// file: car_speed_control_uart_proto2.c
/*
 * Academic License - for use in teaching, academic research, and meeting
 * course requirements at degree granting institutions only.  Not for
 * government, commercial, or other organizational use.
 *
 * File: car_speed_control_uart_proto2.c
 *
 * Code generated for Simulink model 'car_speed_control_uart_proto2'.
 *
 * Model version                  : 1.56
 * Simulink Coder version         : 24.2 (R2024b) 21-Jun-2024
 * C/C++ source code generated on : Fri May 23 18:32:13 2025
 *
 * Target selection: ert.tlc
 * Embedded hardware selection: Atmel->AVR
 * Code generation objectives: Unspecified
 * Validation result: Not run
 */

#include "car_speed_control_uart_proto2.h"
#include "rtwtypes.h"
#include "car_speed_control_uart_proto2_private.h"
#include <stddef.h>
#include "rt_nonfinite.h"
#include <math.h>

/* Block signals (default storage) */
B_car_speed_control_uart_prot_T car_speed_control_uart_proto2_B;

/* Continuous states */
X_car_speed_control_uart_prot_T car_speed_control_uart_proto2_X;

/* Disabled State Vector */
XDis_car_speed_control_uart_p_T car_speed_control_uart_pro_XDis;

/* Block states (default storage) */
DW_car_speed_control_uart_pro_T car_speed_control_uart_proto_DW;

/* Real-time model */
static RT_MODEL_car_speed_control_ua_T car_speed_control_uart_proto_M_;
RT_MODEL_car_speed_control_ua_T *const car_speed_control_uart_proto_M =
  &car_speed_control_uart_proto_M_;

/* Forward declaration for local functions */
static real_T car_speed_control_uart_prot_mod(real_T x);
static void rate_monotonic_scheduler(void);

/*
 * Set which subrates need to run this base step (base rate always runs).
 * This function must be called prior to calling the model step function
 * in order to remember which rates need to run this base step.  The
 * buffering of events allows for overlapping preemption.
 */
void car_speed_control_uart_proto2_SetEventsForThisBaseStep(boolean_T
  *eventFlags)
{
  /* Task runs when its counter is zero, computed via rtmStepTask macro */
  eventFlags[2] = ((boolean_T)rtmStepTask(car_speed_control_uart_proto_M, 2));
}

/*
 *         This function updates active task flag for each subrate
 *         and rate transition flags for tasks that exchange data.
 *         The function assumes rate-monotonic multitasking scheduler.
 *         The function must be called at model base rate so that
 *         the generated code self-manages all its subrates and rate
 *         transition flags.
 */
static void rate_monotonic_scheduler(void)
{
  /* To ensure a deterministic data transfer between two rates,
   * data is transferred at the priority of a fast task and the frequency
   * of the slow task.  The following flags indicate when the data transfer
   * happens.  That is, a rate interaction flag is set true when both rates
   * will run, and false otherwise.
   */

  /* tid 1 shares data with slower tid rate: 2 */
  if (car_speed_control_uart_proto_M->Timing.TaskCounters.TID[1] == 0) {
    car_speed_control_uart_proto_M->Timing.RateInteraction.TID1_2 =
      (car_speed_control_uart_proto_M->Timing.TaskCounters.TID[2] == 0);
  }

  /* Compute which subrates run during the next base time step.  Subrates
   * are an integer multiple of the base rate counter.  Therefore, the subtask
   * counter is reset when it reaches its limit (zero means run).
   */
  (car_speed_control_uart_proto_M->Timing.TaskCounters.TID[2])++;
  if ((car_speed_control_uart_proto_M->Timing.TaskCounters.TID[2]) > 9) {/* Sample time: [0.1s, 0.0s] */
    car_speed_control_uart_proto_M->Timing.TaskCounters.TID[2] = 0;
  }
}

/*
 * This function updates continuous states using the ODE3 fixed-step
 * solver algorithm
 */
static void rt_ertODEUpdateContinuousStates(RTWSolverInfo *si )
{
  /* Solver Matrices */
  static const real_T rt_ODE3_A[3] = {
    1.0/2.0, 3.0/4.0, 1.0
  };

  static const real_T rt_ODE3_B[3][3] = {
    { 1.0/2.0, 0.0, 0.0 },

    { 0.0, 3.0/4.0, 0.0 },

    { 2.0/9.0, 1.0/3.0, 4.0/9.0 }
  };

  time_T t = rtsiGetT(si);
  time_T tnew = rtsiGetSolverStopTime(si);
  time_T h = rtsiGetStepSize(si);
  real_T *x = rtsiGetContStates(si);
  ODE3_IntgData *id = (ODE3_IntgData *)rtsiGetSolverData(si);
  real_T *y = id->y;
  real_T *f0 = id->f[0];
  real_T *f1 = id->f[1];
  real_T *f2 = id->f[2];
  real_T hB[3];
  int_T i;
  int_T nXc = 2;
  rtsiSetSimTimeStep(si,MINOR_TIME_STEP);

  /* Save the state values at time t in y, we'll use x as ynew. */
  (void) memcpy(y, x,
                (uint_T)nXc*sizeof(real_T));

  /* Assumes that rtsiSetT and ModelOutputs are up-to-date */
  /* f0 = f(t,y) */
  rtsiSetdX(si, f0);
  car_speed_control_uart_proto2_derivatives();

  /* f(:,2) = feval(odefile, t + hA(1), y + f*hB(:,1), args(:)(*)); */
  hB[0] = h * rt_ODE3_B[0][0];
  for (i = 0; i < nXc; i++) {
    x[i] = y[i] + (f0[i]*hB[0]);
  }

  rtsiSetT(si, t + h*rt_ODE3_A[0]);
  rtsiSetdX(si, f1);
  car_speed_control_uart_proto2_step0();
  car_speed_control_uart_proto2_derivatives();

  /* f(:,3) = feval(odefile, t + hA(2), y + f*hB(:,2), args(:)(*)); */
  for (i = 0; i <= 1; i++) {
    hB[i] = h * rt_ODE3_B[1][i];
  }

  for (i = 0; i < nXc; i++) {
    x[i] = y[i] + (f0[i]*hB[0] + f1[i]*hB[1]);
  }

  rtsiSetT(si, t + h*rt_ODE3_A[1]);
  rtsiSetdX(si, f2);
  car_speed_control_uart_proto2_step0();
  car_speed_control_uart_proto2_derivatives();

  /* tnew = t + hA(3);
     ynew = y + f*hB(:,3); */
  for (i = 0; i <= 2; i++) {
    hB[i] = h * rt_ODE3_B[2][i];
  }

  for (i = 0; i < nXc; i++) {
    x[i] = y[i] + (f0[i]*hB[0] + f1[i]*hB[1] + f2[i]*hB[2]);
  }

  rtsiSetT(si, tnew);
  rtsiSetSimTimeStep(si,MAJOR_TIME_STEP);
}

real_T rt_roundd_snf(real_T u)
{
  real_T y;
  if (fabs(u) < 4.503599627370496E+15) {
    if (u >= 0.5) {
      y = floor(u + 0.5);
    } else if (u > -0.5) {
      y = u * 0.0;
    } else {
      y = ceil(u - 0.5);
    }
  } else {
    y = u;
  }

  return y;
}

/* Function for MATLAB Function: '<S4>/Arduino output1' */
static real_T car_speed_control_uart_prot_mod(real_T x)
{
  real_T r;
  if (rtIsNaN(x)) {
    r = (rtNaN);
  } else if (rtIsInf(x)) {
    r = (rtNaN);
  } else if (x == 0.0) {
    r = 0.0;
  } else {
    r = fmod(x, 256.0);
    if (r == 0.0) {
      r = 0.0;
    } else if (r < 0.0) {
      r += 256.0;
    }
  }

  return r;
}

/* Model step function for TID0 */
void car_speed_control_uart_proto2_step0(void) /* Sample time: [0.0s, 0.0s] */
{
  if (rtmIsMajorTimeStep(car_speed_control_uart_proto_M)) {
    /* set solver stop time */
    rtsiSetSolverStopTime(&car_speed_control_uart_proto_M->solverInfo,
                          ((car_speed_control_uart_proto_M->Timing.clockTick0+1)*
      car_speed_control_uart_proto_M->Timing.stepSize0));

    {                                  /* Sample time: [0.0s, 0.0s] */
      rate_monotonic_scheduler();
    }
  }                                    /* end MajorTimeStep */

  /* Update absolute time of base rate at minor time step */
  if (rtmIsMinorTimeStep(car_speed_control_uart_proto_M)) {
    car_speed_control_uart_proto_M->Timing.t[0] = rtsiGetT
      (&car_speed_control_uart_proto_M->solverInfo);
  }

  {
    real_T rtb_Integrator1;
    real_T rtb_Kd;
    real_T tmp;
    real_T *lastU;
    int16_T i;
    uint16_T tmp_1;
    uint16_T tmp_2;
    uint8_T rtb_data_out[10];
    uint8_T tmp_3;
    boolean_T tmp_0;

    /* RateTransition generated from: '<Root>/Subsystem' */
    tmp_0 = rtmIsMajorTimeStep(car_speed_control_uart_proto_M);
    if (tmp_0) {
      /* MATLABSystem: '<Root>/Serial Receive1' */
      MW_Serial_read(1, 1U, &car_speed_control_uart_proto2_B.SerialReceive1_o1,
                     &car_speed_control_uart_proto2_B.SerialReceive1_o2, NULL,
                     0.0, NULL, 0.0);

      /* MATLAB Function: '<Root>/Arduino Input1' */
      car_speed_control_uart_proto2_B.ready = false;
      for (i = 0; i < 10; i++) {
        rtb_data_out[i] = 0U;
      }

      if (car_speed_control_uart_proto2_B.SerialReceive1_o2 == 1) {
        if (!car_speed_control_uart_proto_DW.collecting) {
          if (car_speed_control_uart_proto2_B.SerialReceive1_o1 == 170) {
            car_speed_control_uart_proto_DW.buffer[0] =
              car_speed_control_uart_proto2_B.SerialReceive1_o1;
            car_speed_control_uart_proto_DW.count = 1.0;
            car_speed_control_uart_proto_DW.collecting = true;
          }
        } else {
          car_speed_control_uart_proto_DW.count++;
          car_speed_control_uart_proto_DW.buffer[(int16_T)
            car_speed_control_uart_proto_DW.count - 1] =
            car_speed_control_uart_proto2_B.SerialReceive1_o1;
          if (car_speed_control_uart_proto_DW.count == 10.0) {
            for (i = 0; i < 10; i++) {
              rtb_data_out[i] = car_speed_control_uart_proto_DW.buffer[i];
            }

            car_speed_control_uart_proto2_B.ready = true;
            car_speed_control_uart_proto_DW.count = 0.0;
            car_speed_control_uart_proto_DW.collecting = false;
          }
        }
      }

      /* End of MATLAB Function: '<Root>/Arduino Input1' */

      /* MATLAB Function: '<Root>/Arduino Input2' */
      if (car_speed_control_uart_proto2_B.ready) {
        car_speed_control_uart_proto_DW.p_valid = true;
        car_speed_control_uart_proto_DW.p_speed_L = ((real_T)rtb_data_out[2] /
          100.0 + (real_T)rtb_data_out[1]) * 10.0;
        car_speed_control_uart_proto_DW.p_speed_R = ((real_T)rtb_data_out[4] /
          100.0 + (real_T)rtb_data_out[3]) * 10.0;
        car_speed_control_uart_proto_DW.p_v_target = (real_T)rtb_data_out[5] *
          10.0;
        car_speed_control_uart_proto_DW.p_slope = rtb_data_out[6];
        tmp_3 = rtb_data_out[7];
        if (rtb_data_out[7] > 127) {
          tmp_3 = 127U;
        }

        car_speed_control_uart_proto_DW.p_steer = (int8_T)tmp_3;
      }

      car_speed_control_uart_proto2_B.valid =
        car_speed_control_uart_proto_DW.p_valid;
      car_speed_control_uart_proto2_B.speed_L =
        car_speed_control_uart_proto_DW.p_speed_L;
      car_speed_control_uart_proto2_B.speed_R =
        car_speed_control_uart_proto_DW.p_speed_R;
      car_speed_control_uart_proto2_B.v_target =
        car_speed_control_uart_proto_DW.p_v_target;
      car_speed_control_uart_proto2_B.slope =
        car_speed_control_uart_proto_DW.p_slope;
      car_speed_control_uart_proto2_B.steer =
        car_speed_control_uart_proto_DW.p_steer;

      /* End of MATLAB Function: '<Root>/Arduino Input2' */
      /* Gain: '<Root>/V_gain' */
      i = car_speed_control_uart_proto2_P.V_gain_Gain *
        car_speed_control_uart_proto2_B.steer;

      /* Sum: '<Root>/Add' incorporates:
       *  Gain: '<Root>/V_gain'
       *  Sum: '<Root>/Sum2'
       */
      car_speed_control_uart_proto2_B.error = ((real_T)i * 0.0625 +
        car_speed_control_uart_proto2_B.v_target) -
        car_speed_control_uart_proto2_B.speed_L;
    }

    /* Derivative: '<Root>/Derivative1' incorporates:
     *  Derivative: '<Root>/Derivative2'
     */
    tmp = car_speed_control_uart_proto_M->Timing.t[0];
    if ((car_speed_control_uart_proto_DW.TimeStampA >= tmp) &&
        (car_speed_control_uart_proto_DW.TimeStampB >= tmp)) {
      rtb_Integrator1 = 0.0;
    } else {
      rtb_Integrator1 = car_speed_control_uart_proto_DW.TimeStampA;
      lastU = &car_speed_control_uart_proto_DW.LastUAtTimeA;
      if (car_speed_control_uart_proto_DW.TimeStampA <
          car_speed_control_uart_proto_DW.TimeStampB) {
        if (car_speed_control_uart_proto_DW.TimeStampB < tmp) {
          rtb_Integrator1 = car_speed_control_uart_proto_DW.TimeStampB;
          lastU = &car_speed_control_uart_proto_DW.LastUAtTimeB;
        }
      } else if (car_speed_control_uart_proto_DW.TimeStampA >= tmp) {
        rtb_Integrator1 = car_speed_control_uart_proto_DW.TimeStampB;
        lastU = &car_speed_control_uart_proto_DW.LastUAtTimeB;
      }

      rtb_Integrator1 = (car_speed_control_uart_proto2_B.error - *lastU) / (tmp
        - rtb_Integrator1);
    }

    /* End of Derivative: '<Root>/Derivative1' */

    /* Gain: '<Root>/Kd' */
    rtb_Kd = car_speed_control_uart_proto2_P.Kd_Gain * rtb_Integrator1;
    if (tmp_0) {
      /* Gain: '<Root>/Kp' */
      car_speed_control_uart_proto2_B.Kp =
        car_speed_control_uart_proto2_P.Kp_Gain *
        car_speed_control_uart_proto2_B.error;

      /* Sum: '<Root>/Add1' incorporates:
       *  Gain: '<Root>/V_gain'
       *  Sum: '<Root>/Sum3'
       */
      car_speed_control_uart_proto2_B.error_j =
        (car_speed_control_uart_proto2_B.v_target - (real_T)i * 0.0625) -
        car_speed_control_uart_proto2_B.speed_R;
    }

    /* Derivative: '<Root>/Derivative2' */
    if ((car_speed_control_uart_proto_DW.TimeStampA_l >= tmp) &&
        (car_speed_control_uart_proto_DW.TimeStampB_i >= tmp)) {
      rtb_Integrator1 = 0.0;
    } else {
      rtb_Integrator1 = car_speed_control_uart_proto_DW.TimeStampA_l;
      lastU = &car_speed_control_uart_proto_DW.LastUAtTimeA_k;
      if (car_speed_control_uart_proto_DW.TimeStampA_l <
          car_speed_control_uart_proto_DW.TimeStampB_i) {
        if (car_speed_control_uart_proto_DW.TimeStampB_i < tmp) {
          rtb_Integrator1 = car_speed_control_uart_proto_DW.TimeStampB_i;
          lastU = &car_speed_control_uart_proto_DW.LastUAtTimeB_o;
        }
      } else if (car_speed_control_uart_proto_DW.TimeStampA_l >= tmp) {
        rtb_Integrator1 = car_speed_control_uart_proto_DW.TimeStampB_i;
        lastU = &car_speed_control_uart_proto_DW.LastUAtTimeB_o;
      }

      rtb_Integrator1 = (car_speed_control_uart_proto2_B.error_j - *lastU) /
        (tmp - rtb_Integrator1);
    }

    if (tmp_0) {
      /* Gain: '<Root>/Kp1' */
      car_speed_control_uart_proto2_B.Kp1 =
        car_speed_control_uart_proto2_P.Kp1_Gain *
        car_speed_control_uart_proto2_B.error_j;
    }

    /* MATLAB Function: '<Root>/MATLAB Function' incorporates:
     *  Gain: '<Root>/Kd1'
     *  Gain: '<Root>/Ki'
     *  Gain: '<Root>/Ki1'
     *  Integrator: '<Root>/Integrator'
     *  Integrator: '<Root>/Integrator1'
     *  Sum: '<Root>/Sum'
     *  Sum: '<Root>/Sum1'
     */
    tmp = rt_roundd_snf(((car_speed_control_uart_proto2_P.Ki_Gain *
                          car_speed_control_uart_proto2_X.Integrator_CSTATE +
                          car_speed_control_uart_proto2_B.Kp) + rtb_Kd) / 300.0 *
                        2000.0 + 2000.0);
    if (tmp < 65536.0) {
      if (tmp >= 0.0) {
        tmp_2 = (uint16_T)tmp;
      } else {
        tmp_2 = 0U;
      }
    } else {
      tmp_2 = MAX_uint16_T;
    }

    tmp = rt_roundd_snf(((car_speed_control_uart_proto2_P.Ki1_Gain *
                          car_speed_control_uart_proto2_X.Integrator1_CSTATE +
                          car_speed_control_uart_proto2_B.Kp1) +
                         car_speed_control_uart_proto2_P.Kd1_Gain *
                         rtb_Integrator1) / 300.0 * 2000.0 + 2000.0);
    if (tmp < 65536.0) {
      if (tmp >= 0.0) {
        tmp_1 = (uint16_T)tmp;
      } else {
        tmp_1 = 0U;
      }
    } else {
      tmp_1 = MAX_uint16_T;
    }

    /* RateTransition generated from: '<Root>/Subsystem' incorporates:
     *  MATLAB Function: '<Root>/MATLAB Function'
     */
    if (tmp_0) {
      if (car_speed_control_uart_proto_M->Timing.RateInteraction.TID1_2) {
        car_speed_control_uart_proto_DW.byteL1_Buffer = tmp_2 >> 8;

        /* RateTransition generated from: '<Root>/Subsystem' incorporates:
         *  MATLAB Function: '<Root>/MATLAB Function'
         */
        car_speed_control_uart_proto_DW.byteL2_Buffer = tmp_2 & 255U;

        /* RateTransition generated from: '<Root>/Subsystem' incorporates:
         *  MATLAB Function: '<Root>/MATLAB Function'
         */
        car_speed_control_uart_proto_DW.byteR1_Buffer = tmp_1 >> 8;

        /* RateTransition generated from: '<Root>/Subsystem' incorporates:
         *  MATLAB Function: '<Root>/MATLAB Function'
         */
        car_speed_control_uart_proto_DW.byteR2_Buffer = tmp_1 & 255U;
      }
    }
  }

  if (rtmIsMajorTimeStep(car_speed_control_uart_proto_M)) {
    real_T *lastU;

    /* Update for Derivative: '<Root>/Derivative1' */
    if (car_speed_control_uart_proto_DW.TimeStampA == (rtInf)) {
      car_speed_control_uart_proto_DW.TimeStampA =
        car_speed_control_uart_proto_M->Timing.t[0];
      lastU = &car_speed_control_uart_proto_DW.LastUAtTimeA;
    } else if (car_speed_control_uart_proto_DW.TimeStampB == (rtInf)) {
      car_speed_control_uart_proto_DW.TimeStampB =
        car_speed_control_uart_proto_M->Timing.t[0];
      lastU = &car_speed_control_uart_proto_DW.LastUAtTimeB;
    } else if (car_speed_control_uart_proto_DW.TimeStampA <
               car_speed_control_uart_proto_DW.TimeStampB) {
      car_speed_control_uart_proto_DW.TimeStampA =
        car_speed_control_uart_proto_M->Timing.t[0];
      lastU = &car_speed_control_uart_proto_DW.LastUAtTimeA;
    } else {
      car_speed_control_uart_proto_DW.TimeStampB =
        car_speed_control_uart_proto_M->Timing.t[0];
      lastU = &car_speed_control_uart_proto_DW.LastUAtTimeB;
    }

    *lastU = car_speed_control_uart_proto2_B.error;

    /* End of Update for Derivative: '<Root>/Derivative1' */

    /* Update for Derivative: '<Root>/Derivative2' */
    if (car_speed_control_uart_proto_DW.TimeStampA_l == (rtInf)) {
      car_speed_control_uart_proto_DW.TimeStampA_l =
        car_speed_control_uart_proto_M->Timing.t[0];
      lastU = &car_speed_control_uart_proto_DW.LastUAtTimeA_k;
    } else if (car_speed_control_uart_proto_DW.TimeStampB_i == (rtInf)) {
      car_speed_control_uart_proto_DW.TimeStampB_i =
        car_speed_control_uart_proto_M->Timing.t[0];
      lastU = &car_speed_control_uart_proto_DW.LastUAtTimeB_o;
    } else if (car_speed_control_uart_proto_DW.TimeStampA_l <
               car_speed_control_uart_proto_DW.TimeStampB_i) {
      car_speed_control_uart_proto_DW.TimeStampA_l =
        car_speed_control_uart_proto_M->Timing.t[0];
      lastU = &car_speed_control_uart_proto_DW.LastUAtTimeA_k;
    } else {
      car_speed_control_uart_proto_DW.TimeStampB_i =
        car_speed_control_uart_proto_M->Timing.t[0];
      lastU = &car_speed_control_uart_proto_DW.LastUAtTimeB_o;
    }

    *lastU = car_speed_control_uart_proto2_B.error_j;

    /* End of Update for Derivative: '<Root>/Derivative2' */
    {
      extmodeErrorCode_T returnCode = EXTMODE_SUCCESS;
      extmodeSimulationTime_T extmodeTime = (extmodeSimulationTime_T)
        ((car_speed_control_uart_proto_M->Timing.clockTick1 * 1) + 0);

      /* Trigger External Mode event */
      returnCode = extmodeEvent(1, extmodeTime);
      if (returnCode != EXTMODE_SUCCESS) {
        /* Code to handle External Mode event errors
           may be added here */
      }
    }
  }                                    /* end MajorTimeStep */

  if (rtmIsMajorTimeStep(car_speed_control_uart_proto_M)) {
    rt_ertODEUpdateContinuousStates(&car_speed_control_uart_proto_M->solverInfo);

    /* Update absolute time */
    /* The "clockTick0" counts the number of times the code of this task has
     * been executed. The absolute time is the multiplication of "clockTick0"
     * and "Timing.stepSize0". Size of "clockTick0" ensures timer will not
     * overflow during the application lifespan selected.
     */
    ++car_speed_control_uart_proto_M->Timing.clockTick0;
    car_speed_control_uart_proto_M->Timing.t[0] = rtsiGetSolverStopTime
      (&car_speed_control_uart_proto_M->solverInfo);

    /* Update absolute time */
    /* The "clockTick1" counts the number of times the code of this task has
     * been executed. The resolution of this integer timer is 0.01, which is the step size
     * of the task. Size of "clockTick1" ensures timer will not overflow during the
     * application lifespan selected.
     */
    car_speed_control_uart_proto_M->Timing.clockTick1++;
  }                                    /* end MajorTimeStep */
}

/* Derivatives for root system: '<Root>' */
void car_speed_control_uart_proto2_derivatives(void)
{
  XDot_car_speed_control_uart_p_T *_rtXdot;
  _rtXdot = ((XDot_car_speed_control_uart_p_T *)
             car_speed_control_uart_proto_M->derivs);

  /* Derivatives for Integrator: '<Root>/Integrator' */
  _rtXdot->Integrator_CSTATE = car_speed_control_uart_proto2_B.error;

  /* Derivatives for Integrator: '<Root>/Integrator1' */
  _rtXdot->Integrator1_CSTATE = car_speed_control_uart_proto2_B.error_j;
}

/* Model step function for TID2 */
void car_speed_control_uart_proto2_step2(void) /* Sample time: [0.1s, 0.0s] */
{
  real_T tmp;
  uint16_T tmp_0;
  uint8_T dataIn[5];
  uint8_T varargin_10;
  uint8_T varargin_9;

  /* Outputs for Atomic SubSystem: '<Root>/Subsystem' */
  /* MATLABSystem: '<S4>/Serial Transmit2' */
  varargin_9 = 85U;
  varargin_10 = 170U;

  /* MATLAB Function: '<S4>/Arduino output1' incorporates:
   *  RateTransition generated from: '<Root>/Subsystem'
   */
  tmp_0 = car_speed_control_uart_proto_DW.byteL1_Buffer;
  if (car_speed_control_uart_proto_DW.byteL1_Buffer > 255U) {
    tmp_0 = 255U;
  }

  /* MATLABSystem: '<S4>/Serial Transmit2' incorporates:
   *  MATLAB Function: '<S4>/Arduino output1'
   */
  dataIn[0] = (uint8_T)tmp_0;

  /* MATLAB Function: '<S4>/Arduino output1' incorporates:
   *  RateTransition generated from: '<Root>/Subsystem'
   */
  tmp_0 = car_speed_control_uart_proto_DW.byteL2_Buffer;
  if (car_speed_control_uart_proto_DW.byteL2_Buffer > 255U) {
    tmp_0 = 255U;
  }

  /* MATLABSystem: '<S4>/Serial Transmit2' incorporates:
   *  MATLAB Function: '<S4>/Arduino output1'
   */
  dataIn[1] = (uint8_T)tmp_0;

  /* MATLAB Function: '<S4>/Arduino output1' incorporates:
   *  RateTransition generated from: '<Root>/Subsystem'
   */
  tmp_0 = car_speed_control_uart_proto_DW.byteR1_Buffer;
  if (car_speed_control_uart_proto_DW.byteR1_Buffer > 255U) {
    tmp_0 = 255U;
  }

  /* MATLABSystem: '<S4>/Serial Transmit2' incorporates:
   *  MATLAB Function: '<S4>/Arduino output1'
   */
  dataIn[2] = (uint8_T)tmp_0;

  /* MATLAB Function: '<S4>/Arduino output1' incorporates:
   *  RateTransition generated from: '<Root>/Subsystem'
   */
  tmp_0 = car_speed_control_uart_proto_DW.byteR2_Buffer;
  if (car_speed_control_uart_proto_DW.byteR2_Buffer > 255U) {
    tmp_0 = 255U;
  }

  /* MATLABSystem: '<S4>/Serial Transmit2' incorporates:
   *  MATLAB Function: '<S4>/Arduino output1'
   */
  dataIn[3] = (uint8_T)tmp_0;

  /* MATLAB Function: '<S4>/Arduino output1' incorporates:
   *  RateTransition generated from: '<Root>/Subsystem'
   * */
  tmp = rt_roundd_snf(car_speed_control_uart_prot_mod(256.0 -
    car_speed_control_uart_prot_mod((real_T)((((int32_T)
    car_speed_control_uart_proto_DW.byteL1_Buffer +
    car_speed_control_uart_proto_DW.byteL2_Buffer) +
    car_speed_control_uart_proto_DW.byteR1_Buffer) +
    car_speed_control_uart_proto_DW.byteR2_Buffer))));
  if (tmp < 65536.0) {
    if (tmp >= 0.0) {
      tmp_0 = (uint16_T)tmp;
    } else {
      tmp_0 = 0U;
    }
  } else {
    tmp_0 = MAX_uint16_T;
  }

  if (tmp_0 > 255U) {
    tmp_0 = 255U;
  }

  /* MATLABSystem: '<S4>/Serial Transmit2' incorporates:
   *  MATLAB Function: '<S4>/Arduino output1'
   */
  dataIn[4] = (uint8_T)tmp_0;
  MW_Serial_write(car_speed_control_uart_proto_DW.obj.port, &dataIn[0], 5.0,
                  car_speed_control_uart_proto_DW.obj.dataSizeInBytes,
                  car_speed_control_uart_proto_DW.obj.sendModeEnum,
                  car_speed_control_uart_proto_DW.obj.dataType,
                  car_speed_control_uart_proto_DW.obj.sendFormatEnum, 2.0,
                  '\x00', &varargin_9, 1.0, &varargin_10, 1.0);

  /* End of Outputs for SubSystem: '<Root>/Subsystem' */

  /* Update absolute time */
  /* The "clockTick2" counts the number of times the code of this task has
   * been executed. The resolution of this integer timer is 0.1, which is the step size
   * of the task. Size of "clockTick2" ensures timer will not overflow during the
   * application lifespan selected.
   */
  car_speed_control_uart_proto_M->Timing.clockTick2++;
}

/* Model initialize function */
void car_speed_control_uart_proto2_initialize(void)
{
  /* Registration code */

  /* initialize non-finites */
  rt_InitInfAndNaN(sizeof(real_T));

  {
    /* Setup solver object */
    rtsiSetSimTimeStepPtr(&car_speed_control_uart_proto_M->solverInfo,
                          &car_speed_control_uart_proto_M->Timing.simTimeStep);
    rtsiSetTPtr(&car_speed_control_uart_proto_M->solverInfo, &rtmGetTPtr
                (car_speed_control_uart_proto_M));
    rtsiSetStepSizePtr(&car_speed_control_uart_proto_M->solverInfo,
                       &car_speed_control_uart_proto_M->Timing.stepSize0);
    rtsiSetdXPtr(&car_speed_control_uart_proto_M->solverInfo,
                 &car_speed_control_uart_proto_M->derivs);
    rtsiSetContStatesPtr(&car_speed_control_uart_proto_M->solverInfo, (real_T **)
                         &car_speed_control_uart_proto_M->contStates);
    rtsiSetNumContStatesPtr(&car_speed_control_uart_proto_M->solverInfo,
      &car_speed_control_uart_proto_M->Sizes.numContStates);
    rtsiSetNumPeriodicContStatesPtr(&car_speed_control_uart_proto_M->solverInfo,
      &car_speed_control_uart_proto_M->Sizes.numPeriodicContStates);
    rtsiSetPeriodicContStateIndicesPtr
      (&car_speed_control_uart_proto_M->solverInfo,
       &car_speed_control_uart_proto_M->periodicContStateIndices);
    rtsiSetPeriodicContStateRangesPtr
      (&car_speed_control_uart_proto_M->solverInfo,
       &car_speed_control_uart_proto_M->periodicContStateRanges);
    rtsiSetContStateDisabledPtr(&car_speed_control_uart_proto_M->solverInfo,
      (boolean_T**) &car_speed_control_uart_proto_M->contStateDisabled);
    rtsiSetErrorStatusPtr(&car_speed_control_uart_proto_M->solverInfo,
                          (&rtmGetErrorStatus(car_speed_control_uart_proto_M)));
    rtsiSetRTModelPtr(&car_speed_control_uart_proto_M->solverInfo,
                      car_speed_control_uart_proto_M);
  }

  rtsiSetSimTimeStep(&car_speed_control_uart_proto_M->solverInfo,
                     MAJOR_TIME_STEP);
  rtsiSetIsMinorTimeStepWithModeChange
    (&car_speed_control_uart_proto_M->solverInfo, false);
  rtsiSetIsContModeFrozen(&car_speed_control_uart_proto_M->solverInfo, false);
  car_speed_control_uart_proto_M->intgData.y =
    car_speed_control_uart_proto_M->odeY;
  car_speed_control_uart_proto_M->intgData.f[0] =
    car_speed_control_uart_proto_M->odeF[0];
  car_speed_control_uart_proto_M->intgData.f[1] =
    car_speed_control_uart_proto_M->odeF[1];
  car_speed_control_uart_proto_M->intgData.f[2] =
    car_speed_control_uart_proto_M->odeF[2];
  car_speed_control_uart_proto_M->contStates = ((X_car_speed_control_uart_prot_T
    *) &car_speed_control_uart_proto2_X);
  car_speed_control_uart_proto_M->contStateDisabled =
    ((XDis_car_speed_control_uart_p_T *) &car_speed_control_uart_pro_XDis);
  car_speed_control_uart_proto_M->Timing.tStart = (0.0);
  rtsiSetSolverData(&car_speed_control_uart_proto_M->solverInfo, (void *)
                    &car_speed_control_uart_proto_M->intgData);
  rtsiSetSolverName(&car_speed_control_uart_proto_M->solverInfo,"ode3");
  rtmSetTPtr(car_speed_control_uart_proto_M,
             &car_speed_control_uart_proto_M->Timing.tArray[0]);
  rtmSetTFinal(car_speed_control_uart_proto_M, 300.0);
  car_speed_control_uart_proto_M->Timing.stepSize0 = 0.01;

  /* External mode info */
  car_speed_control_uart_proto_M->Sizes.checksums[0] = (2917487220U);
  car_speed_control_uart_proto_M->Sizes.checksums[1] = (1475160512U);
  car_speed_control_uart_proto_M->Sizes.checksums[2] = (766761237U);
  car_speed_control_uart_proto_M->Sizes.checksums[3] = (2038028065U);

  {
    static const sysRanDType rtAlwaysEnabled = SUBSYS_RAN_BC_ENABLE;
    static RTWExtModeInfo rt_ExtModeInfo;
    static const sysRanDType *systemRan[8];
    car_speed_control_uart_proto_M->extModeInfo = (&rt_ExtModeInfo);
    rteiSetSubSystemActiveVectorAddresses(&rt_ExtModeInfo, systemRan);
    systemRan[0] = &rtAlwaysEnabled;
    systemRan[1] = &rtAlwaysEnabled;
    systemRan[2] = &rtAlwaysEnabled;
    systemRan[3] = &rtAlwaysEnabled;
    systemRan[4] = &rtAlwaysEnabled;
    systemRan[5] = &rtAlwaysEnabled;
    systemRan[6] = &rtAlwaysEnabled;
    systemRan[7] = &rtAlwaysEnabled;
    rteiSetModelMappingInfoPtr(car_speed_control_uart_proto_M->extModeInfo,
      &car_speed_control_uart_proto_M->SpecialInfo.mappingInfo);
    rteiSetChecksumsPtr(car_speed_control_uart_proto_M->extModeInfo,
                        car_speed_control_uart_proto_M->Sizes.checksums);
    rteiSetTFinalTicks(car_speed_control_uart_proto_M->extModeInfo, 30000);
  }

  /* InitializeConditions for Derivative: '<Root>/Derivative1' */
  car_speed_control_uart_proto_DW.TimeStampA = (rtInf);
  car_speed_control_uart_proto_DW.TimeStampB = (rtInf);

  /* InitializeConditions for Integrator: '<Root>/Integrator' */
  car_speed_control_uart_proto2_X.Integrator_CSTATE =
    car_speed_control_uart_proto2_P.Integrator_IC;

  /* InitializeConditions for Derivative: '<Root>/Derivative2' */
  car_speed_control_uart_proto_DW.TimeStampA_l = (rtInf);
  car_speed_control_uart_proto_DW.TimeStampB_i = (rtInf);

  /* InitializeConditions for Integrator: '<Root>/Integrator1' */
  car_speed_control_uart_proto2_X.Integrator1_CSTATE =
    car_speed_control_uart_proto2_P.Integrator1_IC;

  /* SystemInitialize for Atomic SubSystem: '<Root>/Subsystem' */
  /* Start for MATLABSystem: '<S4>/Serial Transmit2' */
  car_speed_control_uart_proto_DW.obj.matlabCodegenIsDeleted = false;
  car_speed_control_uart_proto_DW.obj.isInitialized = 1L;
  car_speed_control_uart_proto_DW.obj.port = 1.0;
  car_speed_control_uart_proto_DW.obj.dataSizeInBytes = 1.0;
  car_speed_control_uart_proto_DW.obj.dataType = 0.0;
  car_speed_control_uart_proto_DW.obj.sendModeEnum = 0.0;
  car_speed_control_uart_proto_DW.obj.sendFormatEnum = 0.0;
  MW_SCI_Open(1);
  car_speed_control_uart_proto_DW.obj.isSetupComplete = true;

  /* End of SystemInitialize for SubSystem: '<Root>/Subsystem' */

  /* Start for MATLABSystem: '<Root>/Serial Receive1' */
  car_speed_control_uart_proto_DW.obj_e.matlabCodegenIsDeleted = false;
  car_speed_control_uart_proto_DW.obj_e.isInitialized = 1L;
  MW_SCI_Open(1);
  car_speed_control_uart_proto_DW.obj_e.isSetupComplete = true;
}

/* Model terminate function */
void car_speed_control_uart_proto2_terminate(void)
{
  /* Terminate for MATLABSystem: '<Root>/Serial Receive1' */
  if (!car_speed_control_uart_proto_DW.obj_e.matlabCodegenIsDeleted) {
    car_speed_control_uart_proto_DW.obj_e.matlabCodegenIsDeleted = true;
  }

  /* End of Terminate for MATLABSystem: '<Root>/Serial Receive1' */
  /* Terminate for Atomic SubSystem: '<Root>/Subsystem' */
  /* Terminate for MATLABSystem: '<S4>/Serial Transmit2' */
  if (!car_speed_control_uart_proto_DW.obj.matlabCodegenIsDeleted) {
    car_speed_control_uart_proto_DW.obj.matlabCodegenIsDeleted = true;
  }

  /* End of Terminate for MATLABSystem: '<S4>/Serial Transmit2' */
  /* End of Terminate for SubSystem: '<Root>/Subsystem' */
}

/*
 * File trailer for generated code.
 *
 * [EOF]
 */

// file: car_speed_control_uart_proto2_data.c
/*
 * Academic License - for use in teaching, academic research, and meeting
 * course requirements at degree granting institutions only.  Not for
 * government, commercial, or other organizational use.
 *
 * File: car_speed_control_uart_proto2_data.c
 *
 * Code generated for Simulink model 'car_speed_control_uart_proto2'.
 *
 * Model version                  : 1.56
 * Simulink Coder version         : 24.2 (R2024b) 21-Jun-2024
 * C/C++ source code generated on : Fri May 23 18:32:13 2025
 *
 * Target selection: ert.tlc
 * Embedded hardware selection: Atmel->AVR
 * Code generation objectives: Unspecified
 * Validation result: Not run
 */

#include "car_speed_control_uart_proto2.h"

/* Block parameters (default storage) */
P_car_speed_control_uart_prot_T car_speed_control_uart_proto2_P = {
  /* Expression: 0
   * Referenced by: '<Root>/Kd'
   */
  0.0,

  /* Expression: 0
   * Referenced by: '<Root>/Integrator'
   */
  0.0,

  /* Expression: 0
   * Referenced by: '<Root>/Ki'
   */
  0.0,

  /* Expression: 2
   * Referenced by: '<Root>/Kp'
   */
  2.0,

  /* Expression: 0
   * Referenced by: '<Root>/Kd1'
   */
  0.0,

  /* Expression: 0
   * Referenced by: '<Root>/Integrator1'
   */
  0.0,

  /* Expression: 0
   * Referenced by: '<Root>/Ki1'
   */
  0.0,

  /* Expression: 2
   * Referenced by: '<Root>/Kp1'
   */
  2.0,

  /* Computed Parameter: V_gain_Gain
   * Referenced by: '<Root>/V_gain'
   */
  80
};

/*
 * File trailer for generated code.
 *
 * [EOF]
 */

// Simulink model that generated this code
simulink model "car_speed_control_uart_proto2"  (R2024b)
settings: Solver=FixedStepAuto  StartTime=0.0  StopTime=300  FixedStep=0.01  RelTol=1e-3  EnableMultiTasking=on
libraries: arduinolib x2

== system car_speed_control_uart_proto2 ==
  Add : Sum  Inputs=+-
  Add1 : Sum  Inputs=+-
  Arduino Input1 : MATLAB Function  TreatAsAtomicUnit=on
  Arduino Input2 : MATLAB Function  TreatAsAtomicUnit=on
  Derivative1 : Derivative
  Derivative2 : Derivative
  Display{1,5..11} (8 alike) : Display
  Integrator : Integrator
  Integrator1 : Integrator
  Kd : Gain  Gain=0
  Kd1 : Gain  Gain=0
  Ki : Gain  Gain=0
  Ki1 : Gain  Gain=0
  Kp : Gain  Gain=2
  Kp1 : Gain  Gain=2
  MATLAB Function : MATLAB Function  TreatAsAtomicUnit=on
  Serial Receive1 : arduinolib/Serial Receive  portNumber=1  DataType=uint8  blockPlatform=ARDUINO  TimeOut=0  MaxDataLength=10  isARMArch=off  DataLengthOption=Length via dialog  Datalength=1  Header=[]  Terminator=[]  SampleTime=0.01  ShowOutStatus=on
  Subsystem : Subsystem  TreatAsAtomicUnit=on  SystemSampleTime=0.1
  Sum : Sum  Inputs=|+++
  Sum1 : Sum  Inputs=|+++
  Sum2 : Sum  Inputs=|++
  Sum3 : Sum  Inputs=|+-
  V_gain : Gain  Gain=5
  valid : Display
  valid1 : Display
  wires:
  Arduino Input2/2(speed_L) -> Display6/1, Add/2, Display1/1
  Arduino Input2/4(v_target) -> Sum2/1, Sum3/1, Display8/1
  Add/1 -> Derivative1/1, Integrator/1, Kp/1  "error"
  Integrator/1 -> Ki/1
  Derivative1/1 -> Kd/1
  Kp/1 -> Sum/1
  Ki/1 -> Sum/2
  Kd/1 -> Sum/3
  Sum1/1 -> MATLAB Function/2(vR)
  Arduino Input1/1(ready) -> valid/1, Arduino Input2/1(ready)
  Serial Receive1/2 -> Display11/1, Arduino Input1/2(status)
  Arduino Input1/2(data_out) -> Arduino Input2/2(u)
  Serial Receive1/1 -> valid1/1, Arduino Input1/1(byte_in)
  Arduino Input2/5(slope) -> Display9/1
  Arduino Input2/3(speed_R) -> Add1/2, Display7/1
  Arduino Input2/1(valid) -> Display5/1
  Arduino Input2/6(steer) -> V_gain/1, Display10/1
  Sum/1 -> MATLAB Function/1(vL)
  V_gain/1 -> Sum3/2, Sum2/2
  Sum2/1 -> Add/1
  Sum3/1 -> Add1/1
  Kd1/1 -> Sum1/3
  Ki1/1 -> Sum1/2
  Kp1/1 -> Sum1/1
  Derivative2/1 -> Kd1/1
  Integrator1/1 -> Ki1/1
  Add1/1 -> Kp1/1, Integrator1/1, Derivative2/1  "error"
  MATLAB Function/1(byteL1) -> Subsystem/1(L1)
  MATLAB Function/2(byteL2) -> Subsystem/2(L2)
  MATLAB Function/3(byteR1) -> Subsystem/3(R1)
  MATLAB Function/4(byteR2) -> Subsystem/4(R2)

== system car_speed_control_uart_proto2/Subsystem ==
  L1 : Inport
  L2 : Inport  Port=2
  R1 : Inport  Port=3
  R2 : Inport  Port=4
  Arduino output1 : MATLAB Function  TreatAsAtomicUnit=on
  Serial Transmit2 : arduinolib/Serial Transmit  portNumber=1  sendmode=write  sendformat=Decimal  floatprecision=2  header=[0xAA]  terminator=[0x55]  blockPlatform=ARDUINO
  wires:
  L2/1 -> Arduino output1/2(byteL2)
  Arduino output1/1(frame) -> Serial Transmit2/1
  L1/1 -> Arduino output1/1(byteL1)
  R1/1 -> Arduino output1/3(byteR1)
  R2/1 -> Arduino output1/4(byteR2)

== matlab function car_speed_control_uart_proto2/MATLAB Function ==
function [byteL1, byteL2, byteR1, byteR2] = encode_pwm_duty(vL, vR)
% 입력:
%   vL, vR: mm/s 단위의 속도값 (saturation은 외부에서 처리)
% 출력:
%   byteL1, byteL2: 왼쪽 듀티 (LSB, MSB)
%   byteR1, byteR2: 오른쪽 듀티 (LSB, MSB)

%#codegen
min_duty = 2000;
max_duty = 4000;
v_max = 300;  % 최대 속도(mm/s)

% 왼쪽 듀티 계산
dutyL = uint16(min_duty + (vL / v_max) * (max_duty - min_duty));
byteL2 = bitand(dutyL, 255);         % LSB
byteL1 = bitshift(dutyL, -8);        % MSB

% 오른쪽 듀티 계산
dutyR = uint16(min_duty + (vR / v_max) * (max_duty - min_duty));
byteR2 = bitand(dutyR, 255);
byteR1 = bitshift(dutyR, -8);

== matlab function car_speed_control_uart_proto2/Arduino Input2 ==
function [valid, speed_L, speed_R, v_target, slope, steer] = parseUART_persistent(ready, u)
% UART 패킷 파서 (persistent 방식으로 이전 값 유지)
% u: [10x1] uint8, 패킷 데이터
% ready: 패킷 유효 신호

%#codegen

% 이전 출력값 저장용 persistent 변수
persistent p_valid p_speed_L p_speed_R p_v_target p_slope p_steer

% 초기화 (최초 실행 시)
if isempty(p_valid)
    p_valid = false;
    p_speed_L = 0.0;
    p_speed_R = 0.0;
    p_v_target = 0.0;
    p_slope = uint8(0);
    p_steer = int8(0);
end

% 새로운 데이터가 들어왔을 경우만 업데이트
if ready == 1
        p_valid = true;
        p_speed_L = (double(u(2)) + double(u(3))/100) * 10;
        p_speed_R = (double(u(4)) + double(u(5))/100) * 10;
        p_v_target = double(u(6))*10;
        p_slope = u(7);
        p_steer = int8(u(8));
end

% 항상 마지막 유효 출력 반환
valid     = p_valid;
speed_L   = p_speed_L;
speed_R   = p_speed_R;
v_target  = p_v_target;
slope     = p_slope;
steer     = p_steer;

== matlab function car_speed_control_uart_proto2/Arduino Input1 ==
function [ready, data_out] = uart_parser(byte_in, status)
% UART 프레임 수신기 (Start Byte = 0xAA, Total = 10 bytes)
% 입력: byte_in - 1바이트씩 들어오는 uint8
% 입력: status - Serial Receive의 상태 (1이면 수신 성공)
% 출력: ready - 1이면 패킷 파싱 완료
% 출력: data_out - [1x10] uint8, 패킷 데이터

persistent buffer count collecting

if isempty(buffer)
    buffer = zeros(1, 10, 'uint8');
    count = 0;
    collecting = false;
end

ready = false;
data_out = zeros(1,10,'uint8');

if status == 1
    if ~collecting
        % 아직 수집 시작 전 → start byte 찾기
        if byte_in == hex2dec('AA')
            buffer(1) = byte_in;
            count = 1;
            collecting = true;
        end
    else
        % 수집 중
        count = count + 1;
        buffer(count) = byte_in;

        if count == 10
            data_out = buffer;
            ready = true;
            count = 0;
            collecting = false;
        end
    end
end

== matlab function car_speed_control_uart_proto2/Subsystem/Arduino output1 ==
function frame = makeFrame(byteL1, byteL2, byteR1, byteR2)
% 입력:
%   byteL1, byteL2 : 왼쪽 듀티 (LSB, MSB)
%   byteR1, byteR2 : 오른쪽 듀티 (LSB, MSB)
% 출력:
%   frame: 5-byte UART 프레임 [L_LSB, L_MSB, R_LSB, R_MSB, CRC]

% CRC 계산: 256 - mod(sum(data), 256)
data_sum = double(byteL1) + double(byteL2) + double(byteR1) + double(byteR2);
crc = mod(256 - mod(data_sum, 256), 256);

% 프레임 구성
frame = uint8([byteL1, byteL2, byteR1, byteR2, crc]);
end
